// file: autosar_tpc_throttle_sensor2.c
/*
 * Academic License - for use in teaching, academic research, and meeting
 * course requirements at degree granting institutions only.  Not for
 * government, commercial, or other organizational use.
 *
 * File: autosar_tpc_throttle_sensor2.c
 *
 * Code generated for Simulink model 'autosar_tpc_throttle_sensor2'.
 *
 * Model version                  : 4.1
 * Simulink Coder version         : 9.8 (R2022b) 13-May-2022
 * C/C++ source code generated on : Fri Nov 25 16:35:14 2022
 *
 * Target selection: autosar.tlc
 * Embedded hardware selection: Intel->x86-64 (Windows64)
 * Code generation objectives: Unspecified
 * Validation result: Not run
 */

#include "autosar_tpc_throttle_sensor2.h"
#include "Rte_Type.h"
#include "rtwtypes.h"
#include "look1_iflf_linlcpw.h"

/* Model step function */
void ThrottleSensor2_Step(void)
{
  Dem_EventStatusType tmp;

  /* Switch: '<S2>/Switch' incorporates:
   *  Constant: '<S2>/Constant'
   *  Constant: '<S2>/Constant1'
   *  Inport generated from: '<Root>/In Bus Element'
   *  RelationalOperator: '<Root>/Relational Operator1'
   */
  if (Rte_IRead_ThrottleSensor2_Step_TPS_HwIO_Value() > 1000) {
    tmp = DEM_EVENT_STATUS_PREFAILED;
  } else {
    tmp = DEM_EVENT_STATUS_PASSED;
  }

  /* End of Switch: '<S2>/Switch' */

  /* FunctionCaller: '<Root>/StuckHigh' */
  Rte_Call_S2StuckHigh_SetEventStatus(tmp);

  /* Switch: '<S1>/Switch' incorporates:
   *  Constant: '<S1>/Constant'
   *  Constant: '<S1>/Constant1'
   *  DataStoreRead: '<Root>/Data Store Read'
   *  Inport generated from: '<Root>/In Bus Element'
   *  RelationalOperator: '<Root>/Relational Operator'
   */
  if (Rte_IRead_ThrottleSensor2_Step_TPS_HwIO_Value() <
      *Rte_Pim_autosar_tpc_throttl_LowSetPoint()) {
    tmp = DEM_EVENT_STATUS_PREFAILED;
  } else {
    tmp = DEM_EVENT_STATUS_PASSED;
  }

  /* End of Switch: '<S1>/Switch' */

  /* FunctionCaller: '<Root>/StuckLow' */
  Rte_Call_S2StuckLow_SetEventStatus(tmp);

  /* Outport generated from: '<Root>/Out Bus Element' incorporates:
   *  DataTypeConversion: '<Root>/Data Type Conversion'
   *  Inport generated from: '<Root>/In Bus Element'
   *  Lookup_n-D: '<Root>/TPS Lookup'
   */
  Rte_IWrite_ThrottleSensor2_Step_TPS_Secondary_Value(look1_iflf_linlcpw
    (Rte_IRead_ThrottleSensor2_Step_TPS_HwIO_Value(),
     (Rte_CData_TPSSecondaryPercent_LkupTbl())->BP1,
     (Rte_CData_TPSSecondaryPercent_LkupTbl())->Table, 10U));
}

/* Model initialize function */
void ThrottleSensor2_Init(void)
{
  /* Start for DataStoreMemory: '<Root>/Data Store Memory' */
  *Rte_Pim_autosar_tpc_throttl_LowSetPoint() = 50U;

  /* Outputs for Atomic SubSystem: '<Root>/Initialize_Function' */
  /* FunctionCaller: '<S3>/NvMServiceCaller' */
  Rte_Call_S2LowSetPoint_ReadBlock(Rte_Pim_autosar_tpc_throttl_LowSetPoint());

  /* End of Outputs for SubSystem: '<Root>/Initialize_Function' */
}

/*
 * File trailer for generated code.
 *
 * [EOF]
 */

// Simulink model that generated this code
simulink model "autosar_tpc_throttle_sensor2"  (R2022a)
settings: Solver=FixedStepDiscrete  StartTime=0.0  StopTime=10.0  FixedStep=0.005  RelTol=1e-3
model workspace (MATLAB code in the model file + MAT data in the model file):
  TPSPercent_LkupTbl = Simulink.LookupTable
  TPSPercent_LkupTbl.Table.DataType = 'single'
  TPSPercent_LkupTbl.Table.Min = []
  TPSPercent_LkupTbl.Table.Max = []
  TPSPercent_LkupTbl.Table.Unit = ''
  TPSPercent_LkupTbl.Table.FieldName = 'Table'
  TPSPercent_LkupTbl.Table.Description = ''
  TPSPercent_LkupTbl.Table.Value = [0 10 20 30 40 50 60 70 80 90 100]
  TPSPercent_LkupTbl.BreakpointsSpecification = 'Explicit values'
  TPSPercent_LkupTbl.SupportTunableSize = false
  TPSPercent_LkupTbl.Breakpoints.DataType = 'single'
  TPSPercent_LkupTbl.Breakpoints.Min = []
  TPSPercent_LkupTbl.Breakpoints.Max = []
  TPSPercent_LkupTbl.Breakpoints.Unit = ''
  TPSPercent_LkupTbl.Breakpoints.FieldName = 'BP1'
  TPSPercent_LkupTbl.Breakpoints.Description = ''
  TPSPercent_LkupTbl.Breakpoints.Value = single(linspace(170, 966, 11))
  TPSPercent_LkupTbl.Breakpoints.TunableSizeName = 'N1'
  TPSPercent_LkupTbl.CoderInfo.StorageClass = 'Auto'
  TPSPercent_LkupTbl.StructTypeInfo.Name = 'MyStruct'
  TPSPercent_LkupTbl.StructTypeInfo.DataScope = 'Auto'
  TPSPercent_LkupTbl.StructTypeInfo.HeaderFileName = ''
  TPSSecondaryPercent_LkupTbl : Simulink.LookupTable (value not decoded)
undefined symbols (not defined in the file or in its folder): Dem_EventStatusType, TPSPercentBkpt, TPSPercentTbl
libraries: autosarlibdem x2, autosarlibnvm x1

== system autosar_tpc_throttle_sensor2 ==
  note: Copyright 2019-2020 The MathWorks, Inc.
  In Bus Element : Inport  PortName=TPS_HwIO  Element=Value
  BoolToEventStatus : Subsystem
  BoolToEventStatus1 : Subsystem
  Constant1 : Constant  Value=1000
  Data Store Memory : DataStoreMemory  DataStoreName=LowSetPoint  InitialValue=50  ShowAdditionalParam=off
  Data Store Read : DataStoreRead  DataStoreName=LowSetPoint  IndexOptions=Index vector (dialog)  Indices=1  OutputSizes=1
  Data Type Conversion : DataTypeConversion  OutDataTypeStr=single  SaturateOnIntegerOverflow=off  RndMeth=Floor
  Initialize_Function : Subsystem  TreatAsAtomicUnit=on
  Relational Operator : RelationalOperator  Operator=<  OutDataTypeStr=boolean  InputSameDT=off
  Relational Operator1 : RelationalOperator  Operator=>  OutDataTypeStr=boolean  InputSameDT=off
  StuckHigh : autosarlibdem/DiagnosticMonitorCaller  PortName=S2StuckHigh  Operation=SetEventStatus  Datatype=Enum: Dem_EventStatusType  st=-1  ServiceImpl=autosar.bsw.DemDiagnosticMonitor
  StuckLow : autosarlibdem/DiagnosticMonitorCaller  PortName=S2StuckLow  Operation=SetEventStatus  Datatype=Enum: Dem_EventStatusType  st=-1  ServiceImpl=autosar.bsw.DemDiagnosticMonitor
  TPS Lookup : Lookup_n-D  NumberOfTableDimensions=1  DataSpecification=Lookup table object  LookupTableObject=TPSSecondaryPercent_LkupTbl  BreakpointsForDimension1=TPSPercentBkpt  BreakpointsForDimension1DataTypeStr=single  IndexSearchMethod=Linear search  Table=TPSPercentTbl  TableDataTypeStr=single  ExtrapMethod=Clip  InternalRulePriority=Speed  OutDataTypeStr=single  RndMeth=Simplest
  Terminator : Terminator
  Terminator1 : Terminator
  Out Bus Element : Outport  VectorParamsAs1DForOutWhenUnconnected=off  PortName=TPS_Secondary  Element=Value
  Scope : Scope
  wires:
  TPS Lookup/1 -> Out Bus Element/1
  Data Type Conversion/1 -> TPS Lookup/1
  StuckHigh/1 -> Terminator1/1
  Relational Operator/1 -> BoolToEventStatus/1(FailCondition)
  StuckLow/1 -> Terminator/1
  In Bus Element/1 -> Relational Operator1/1, Relational Operator/1, Data Type Conversion/1
  Constant1/1 -> Relational Operator1/2
  Relational Operator1/1 -> BoolToEventStatus1/1(FailCondition)
  BoolToEventStatus/1(EventStatus) -> StuckLow/1
  Data Store Read/1 -> Relational Operator/2
  BoolToEventStatus1/1(EventStatus) -> StuckHigh/1

== system autosar_tpc_throttle_sensor2/BoolToEventStatus ==
  FailCondition : Inport
  Constant : Constant  Value=Dem_EventStatusType.DEM_EVENT_STATUS_PASSED
  Constant1 : Constant  Value=Dem_EventStatusType.DEM_EVENT_STATUS_PREFAILED
  Switch : Switch  Criteria=u2 ~= 0  SaturateOnIntegerOverflow=off  InputSameDT=off
  EventStatus : Outport  VectorParamsAs1DForOutWhenUnconnected=off
  wires:
  FailCondition/1 -> Switch/2
  Constant/1 -> Switch/3
  Constant1/1 -> Switch/1
  Switch/1 -> EventStatus/1

== system autosar_tpc_throttle_sensor2/BoolToEventStatus1 ==
  FailCondition : Inport
  Constant : Constant  Value=Dem_EventStatusType.DEM_EVENT_STATUS_PASSED
  Constant1 : Constant  Value=Dem_EventStatusType.DEM_EVENT_STATUS_PREFAILED
  Switch : Switch  Criteria=u2 ~= 0  SaturateOnIntegerOverflow=off  InputSameDT=off
  EventStatus : Outport  VectorParamsAs1DForOutWhenUnconnected=off
  wires:
  Switch/1 -> EventStatus/1
  Constant1/1 -> Switch/1
  Constant/1 -> Switch/3
  FailCondition/1 -> Switch/2

== system autosar_tpc_throttle_sensor2/Initialize_Function ==
  Data Store Write : DataStoreWrite  DataStoreName=LowSetPoint  IndexOptions=Index vector (dialog)  Indices=1  OutputSizes=1
  Event Listener : EventListener  DisableCoverage=on  EventName=reset
  NvMServiceCaller : autosarlibnvm/NvMServiceCaller  PortName=S2LowSetPoint  Operation=ReadBlock  ArgumentSpecification=uint8(1)  st=-1  ServiceImpl=autosar.bsw.NvMService
  Terminator : Terminator
  wires:
  NvMServiceCaller/2 -> Terminator/1
  NvMServiceCaller/1 -> Data Store Write/1
